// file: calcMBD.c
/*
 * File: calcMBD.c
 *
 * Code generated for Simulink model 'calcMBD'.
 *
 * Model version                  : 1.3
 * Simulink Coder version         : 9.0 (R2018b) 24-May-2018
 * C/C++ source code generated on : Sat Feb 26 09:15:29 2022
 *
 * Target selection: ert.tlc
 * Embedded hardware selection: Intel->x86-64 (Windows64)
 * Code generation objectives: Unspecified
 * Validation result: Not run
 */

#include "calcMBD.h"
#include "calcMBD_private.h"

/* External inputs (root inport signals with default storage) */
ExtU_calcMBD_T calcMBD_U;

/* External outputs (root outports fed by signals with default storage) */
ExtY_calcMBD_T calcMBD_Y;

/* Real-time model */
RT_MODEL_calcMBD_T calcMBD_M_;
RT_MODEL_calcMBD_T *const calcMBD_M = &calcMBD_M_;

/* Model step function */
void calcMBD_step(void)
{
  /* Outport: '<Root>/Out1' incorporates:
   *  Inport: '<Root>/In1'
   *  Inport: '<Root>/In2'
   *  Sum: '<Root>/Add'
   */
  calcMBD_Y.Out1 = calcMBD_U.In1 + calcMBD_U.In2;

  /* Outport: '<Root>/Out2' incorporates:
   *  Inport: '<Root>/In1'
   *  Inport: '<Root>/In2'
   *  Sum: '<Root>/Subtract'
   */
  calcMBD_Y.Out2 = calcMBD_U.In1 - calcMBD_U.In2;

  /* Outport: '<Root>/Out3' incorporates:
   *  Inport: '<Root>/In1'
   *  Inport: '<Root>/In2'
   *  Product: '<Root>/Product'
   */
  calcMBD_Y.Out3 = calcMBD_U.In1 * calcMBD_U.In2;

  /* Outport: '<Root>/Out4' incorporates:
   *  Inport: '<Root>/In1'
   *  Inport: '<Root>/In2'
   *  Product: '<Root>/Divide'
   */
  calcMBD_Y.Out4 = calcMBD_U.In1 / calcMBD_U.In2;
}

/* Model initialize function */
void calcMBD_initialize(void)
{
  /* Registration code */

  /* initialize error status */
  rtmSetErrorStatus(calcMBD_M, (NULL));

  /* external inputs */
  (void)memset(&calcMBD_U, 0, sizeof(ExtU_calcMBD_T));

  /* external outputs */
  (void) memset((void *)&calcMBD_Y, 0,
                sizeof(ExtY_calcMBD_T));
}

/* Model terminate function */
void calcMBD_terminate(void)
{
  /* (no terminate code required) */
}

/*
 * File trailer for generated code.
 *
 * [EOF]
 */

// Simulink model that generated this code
simulink model "calcMBD"  (R2018b)
settings: Solver=FixedStepDiscrete  StartTime=0.0  StopTime=10.0  RelTol=1e-3

== system calcMBD ==
  In1 : Inport
  In2 : Inport  Port=2
  Add : Sum
  Divide : Product  Inputs=*/
  Product : Product
  Subtract : Sum  Inputs=+-
  Out1 : Outport
  Out2 : Outport  Port=2
  Out3 : Outport  Port=3
  Out4 : Outport  Port=4
  wires:
  In1/1 -> Divide/1, Product/1, Subtract/1, Add/1
  In2/1 -> Divide/2, Product/2, Add/2, Subtract/2
  Divide/1 -> Out4/1
  Product/1 -> Out3/1
  Subtract/1 -> Out2/1
  Add/1 -> Out1/1
